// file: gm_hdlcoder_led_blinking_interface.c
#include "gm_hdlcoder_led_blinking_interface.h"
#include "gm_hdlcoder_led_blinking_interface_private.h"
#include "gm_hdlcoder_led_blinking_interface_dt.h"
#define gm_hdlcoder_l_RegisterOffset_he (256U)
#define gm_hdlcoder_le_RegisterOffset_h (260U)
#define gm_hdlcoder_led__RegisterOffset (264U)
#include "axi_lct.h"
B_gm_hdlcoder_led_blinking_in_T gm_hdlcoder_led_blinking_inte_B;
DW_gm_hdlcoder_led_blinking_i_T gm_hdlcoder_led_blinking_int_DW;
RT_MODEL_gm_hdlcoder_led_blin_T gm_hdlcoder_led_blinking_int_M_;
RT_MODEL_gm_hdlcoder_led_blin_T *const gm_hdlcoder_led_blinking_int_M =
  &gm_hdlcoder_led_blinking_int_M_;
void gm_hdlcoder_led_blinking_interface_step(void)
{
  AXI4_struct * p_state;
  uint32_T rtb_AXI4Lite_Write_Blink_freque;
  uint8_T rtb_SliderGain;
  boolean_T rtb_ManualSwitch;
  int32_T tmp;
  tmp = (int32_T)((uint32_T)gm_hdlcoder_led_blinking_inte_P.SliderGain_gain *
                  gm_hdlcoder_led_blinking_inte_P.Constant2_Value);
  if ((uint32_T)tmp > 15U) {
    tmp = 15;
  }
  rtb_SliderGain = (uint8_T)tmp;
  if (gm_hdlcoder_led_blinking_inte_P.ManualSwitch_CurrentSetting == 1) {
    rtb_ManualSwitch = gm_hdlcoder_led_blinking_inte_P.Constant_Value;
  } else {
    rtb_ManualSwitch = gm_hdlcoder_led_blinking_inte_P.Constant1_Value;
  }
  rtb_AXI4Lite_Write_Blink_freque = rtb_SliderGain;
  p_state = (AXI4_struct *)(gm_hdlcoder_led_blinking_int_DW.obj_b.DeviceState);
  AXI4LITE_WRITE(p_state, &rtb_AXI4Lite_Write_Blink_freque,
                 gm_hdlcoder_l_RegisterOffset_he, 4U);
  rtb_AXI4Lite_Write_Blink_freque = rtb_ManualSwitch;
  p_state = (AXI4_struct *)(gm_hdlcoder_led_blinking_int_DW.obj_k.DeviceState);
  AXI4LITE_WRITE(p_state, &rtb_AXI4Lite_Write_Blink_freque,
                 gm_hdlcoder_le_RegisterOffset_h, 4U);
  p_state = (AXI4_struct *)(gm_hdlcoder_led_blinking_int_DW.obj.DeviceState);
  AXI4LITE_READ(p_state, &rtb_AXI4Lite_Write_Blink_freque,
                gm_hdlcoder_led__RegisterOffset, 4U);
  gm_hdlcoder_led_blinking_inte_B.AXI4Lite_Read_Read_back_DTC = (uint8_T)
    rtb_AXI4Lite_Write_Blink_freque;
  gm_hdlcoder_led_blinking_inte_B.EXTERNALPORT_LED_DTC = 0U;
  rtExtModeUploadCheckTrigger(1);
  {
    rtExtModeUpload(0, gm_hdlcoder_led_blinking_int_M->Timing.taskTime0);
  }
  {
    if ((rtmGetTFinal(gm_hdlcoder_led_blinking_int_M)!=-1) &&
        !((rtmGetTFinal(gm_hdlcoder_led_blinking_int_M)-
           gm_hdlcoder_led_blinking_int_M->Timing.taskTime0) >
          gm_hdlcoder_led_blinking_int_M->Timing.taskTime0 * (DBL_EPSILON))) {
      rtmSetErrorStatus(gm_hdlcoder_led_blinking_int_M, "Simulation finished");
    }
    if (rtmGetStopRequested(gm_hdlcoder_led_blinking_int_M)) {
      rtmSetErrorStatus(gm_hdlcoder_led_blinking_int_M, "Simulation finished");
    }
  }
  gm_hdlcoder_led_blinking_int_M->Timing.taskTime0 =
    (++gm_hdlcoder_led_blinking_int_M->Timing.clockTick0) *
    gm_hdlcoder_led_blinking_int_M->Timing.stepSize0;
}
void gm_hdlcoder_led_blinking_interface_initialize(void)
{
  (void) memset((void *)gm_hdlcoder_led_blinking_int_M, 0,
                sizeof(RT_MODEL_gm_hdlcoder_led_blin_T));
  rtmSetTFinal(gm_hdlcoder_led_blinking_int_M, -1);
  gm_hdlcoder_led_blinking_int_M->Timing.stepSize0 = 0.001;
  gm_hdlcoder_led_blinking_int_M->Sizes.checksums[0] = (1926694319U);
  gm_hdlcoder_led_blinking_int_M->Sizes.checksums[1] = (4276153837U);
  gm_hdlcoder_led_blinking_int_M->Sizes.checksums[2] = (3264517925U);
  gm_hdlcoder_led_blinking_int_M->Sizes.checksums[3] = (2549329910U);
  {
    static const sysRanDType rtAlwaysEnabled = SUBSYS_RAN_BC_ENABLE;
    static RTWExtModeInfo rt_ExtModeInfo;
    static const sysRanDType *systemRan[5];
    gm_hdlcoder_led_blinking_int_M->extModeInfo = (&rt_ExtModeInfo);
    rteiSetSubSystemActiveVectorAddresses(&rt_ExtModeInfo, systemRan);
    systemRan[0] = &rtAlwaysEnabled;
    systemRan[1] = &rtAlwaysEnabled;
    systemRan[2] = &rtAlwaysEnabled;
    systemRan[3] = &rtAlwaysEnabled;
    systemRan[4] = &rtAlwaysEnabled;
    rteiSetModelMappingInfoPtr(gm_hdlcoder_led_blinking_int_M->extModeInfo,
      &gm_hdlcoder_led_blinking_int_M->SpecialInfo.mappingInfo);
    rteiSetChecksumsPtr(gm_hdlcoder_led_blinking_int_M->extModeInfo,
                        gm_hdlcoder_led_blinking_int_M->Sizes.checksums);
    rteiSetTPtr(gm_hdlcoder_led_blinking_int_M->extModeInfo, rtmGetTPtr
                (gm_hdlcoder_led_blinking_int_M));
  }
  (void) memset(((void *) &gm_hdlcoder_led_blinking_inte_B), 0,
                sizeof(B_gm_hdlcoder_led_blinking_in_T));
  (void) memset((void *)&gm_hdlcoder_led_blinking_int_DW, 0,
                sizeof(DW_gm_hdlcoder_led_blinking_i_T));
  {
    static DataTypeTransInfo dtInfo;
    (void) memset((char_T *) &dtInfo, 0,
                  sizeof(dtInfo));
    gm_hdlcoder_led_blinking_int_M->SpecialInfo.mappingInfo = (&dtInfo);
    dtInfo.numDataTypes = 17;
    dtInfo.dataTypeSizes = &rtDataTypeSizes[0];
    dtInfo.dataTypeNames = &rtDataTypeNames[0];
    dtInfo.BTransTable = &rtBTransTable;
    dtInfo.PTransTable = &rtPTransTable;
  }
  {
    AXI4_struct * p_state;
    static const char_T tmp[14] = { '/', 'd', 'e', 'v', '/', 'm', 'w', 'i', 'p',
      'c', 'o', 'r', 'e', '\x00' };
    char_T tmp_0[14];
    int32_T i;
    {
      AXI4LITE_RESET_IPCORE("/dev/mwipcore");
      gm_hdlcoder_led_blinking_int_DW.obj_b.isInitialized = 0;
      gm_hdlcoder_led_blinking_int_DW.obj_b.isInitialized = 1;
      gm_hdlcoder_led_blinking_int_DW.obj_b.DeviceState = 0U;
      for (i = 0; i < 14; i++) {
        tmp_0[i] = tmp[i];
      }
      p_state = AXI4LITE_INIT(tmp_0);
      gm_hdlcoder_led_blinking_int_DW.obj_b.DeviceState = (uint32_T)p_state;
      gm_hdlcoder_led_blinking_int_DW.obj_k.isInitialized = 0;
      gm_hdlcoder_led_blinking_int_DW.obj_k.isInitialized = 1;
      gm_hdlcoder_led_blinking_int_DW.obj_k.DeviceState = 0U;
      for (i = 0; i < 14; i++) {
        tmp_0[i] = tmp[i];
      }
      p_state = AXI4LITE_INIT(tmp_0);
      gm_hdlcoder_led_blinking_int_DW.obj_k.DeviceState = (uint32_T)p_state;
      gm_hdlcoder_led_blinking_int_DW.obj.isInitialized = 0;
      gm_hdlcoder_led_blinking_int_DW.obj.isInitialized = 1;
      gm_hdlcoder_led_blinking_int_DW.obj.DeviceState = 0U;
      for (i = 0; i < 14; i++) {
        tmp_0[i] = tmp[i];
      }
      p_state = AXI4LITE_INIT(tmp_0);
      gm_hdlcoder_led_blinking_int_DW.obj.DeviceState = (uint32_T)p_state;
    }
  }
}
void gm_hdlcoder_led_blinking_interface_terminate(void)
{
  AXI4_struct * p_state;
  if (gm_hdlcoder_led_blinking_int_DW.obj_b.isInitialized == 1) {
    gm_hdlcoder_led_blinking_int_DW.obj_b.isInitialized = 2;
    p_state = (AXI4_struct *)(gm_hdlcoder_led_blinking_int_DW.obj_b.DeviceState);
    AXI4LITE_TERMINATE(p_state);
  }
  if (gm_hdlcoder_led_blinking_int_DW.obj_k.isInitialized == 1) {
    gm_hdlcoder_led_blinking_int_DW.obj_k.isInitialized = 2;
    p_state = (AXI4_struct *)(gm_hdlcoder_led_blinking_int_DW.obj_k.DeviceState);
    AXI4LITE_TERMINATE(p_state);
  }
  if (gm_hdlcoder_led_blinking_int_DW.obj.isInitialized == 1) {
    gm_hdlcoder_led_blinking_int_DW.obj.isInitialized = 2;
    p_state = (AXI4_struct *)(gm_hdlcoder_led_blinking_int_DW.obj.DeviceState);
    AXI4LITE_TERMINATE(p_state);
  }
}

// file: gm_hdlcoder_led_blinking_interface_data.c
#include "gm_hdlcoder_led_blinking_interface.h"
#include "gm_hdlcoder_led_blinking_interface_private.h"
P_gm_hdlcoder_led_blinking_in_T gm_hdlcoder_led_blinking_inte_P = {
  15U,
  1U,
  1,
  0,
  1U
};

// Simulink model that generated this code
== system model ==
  AXI4InterfaceWrite#1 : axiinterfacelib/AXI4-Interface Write  <- 1: DataTypeConversion#1
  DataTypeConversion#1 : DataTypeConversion  <- 1: SliderGain
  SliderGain : simulink/Math Operations/Slider Gain  <- 1: Constant2
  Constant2 : Constant
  AXI4InterfaceWrite#2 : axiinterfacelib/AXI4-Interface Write  <- 1: DataTypeConversion#2
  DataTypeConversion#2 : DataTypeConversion  <- 1: ManualSwitch
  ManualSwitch : ManualSwitch  <- 1: Constant, 2: Constant1
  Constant : Constant
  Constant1 : Constant  Value=0
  AXI4Lite_Read_Read_back_DTC : DataTypeConversion  <- 1: AXI4Lite_Read_Read_back
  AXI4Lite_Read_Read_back : axiinterfacelib/AXI4-Interface Read
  EXTERNALPORT_LED_DTC : DataTypeConversion
